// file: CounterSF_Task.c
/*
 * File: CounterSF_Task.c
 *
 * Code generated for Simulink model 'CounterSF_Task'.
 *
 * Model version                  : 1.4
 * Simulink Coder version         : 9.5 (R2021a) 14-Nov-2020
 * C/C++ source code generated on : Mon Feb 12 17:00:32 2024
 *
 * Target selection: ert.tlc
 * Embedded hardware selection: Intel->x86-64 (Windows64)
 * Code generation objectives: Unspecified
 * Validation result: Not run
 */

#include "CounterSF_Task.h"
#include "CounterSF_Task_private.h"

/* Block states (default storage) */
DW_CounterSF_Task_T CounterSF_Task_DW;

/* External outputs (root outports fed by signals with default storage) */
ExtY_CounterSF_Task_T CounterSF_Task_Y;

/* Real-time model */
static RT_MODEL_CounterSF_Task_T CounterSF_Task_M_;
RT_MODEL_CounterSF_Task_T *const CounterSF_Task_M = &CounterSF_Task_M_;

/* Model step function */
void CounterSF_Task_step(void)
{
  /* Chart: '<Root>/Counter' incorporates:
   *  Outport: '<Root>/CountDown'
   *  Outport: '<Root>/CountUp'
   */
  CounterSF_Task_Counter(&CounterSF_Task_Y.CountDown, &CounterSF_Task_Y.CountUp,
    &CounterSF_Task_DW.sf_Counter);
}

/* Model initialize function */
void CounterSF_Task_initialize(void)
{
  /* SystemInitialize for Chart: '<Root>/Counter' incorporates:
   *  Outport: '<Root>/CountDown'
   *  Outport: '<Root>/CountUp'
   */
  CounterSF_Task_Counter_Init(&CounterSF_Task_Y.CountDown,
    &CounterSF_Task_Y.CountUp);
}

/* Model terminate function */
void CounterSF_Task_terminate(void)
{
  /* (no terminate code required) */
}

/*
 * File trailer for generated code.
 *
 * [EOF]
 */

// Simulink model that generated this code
simulink model "CounterSF_Task"  (R2021a)
settings: Solver=FixedStepDiscrete  StartTime=0.0  StopTime=10.0  RelTol=1e-3

== system CounterSF_Task ==
  Counter : Stateflow chart  TreatAsAtomicUnit=on
  Scope : Scope  NumInputPorts=2
  CountDown : Outport
  CountUp : Outport  Port=2
  wires:
  Counter/2(CountUp) -> Scope/2, CountUp/1
  Counter/1(CountDown) -> Scope/1, CountDown/1

== stateflow chart CounterSF_Task/Counter ==
  state CountUp_And_Down_Modifier
    entry:
    CountUp = CountUp + 1;
    CountDown = CountDown - 1;
  state Reset
    entry:
    CountUp = 0;
    CountDown = 10;
  (default) -> CountUp_And_Down_Modifier
  CountUp_And_Down_Modifier -> CountUp_And_Down_Modifier [order 2] : after(1,tick)
  Reset -> CountUp_And_Down_Modifier
  CountUp_And_Down_Modifier -> Reset [order 1] : [CountUp == 10]
  data: CountDown output =11; CountUp output =-1
